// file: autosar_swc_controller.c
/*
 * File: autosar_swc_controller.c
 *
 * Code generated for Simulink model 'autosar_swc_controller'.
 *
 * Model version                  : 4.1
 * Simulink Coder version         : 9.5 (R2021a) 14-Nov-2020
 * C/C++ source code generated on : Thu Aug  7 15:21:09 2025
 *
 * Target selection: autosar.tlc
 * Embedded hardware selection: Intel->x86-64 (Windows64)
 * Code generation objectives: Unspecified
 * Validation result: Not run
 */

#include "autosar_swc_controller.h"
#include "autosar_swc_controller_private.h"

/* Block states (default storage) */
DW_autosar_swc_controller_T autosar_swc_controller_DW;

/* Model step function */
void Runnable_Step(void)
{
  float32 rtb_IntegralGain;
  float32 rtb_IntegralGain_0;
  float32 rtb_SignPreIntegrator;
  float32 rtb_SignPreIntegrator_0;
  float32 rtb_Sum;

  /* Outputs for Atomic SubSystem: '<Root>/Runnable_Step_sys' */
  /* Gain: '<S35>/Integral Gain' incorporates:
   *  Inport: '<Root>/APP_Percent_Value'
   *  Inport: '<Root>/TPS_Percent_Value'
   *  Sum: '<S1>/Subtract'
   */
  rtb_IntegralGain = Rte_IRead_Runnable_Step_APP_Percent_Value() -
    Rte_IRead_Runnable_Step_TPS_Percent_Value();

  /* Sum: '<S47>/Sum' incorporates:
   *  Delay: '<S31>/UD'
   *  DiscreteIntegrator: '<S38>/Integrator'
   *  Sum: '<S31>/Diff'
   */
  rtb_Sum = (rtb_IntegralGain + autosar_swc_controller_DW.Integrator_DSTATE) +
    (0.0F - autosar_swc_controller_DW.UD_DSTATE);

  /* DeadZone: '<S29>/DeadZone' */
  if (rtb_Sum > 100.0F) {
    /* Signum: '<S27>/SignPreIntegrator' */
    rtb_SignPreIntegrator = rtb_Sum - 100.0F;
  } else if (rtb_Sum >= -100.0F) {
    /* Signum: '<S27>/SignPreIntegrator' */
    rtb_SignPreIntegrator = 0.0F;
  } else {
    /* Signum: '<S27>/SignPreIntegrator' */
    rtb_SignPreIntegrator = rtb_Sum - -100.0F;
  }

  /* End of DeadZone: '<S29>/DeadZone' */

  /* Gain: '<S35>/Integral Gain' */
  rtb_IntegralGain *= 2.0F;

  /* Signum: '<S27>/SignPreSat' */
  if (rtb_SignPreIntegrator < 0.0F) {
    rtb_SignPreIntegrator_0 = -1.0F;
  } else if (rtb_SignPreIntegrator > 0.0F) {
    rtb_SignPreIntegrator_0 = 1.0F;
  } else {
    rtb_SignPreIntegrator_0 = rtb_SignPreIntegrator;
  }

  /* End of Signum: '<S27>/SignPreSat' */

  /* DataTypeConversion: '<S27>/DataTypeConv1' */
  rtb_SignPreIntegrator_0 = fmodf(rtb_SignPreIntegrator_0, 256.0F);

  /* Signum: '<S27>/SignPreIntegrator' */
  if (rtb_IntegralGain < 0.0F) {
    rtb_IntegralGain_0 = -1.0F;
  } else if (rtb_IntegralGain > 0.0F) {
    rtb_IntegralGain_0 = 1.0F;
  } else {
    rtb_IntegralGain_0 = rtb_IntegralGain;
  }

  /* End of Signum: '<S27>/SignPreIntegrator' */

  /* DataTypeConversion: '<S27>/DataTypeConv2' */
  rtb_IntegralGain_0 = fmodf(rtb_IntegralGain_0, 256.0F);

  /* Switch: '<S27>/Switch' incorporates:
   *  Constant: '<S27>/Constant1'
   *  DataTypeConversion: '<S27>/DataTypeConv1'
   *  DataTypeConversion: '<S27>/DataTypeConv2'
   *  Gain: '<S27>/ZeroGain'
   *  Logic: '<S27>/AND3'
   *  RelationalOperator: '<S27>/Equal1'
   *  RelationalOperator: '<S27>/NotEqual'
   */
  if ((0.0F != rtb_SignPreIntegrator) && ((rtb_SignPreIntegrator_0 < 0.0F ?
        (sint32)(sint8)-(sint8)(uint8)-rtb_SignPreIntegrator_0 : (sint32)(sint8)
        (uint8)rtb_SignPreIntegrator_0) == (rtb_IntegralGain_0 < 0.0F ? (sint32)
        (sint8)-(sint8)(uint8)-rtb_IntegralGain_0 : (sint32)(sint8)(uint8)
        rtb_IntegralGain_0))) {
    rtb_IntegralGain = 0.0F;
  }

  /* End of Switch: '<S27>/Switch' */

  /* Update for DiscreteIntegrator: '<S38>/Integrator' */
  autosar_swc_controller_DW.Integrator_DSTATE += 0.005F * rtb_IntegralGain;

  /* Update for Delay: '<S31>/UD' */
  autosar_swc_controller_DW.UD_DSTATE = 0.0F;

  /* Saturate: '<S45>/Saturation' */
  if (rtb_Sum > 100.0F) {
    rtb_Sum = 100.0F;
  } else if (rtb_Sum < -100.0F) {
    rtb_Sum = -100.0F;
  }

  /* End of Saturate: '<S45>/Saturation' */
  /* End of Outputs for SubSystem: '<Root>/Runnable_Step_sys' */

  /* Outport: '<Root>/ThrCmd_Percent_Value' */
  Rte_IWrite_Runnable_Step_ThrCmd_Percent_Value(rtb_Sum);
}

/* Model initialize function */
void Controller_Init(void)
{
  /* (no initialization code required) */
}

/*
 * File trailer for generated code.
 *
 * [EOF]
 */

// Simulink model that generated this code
simulink model "autosar_swc_controller"  (R2021a)
settings: Solver=FixedStepDiscrete  StartTime=0.0  StopTime=10.0  FixedStep=0.005  RelTol=1e-3
libraries: pid_lib x1

== system autosar_swc_controller ==
  note: Copyright 2017 The MathWorks, Inc.
  TPS_Percent_Value : Inport  OutDataTypeStr=single  PortDimensions=1
  APP_Percent_Value : Inport  Port=2  OutDataTypeStr=single  PortDimensions=1
  Runnable_Step_sys : Subsystem  TreatAsAtomicUnit=on  SystemSampleTime=0.005
  ThrCmd_Percent_Value : Outport  OutDataTypeStr=single  PortDimensions=1  VectorParamsAs1DForOutWhenUnconnected=off
  wires:
  TPS_Percent_Value/1 -> Runnable_Step_sys/1(TPS_Percent_Value_read)
  APP_Percent_Value/1 -> Runnable_Step_sys/2(APP_Percent_Value_read)
  Runnable_Step_sys/1(ThrCmd_Percent_Value_write) -> ThrCmd_Percent_Value/1

== system autosar_swc_controller/Runnable_Step_sys ==
  TPS_Percent_Value_read : Inport
  APP_Percent_Value_read : Inport  Port=2
  Discrete PID Controller : pid_lib/PID Controller  Controller=PID  Form=Parallel  TimeDomain=Discrete-time  UseExternalTs=off  SampleTime=-1  IntegratorMethod=Forward Euler  FilterMethod=Forward Euler  ControllerParametersSource=internal  P=1  I=2  D=0  UseFilter=off  N=100  TunerSelectOption=Transfer Function Based (PID Tuner App)  InitialConditionSource=internal  InitialConditionForIntegrator=0  InitialConditionForFilter=0  DifferentiatorICPrevScaledInput=0  ExternalReset=none  TrackingMode=off  Kt=1  LimitOutput=on  SatLimitsSource=internal  UpperSaturationLimit=100  LowerSaturationLimit=-100  LinearizeAsGain=off  AntiWindupMode=clamping  Kb=1  POutMin=[]  POutMax=[]  IOutMin=[]  IOutMax=[]  DOutMin=[]  DOutMax=[]  NOutMin=[]  NOutMax=[]  SumOutMin=[]  SumOutMax=[]  SaturationOutMin=[]  SaturationOutMax=[]  PParamMin=[]  PParamMax=[]  IParamMin=[]  IParamMax=[]  DParamMin=[]  DParamMax=[]  NParamMin=[]  NParamMax=[]  KbParamMin=[]  KbParamMax=[]  KtParamMin=[]  KtParamMax=[]  KbOutMin=[]  KbOutMax=[]  KtOutMin=[]  KtOutMax=[]  IntegratorOutMin=[]  IntegratorOutMax=[]  FilterOutMin=[]  FilterOutMax=[]  SumI1OutMin=[]  SumI1OutMax=[]  SumI2OutMin=[]  SumI2OutMax=[]  SumI3OutMin=[]  SumI3OutMax=[]  SumI4OutMin=[]  SumI4OutMax=[]  SumDOutMin=[]  SumDOutMax=[]  DifferentiatorOutMin=[]  DifferentiatorOutMax=[]  FilterDiffOutCoefMin=[]  FilterDiffOutCoefMax=[]  ReciprocalOutMin=[]  ReciprocalOutMax=[]  SumDenOutMin=[]  SumDenOutMax=[]  SumNumOutMin=[]  SumNumOutMax=[]  DivideOutMin=[]  DivideOutMax=[]  UdiffTsProdOutMin=[]  UdiffTsProdOutMax=[]  NTsProdOutMin=[]  NTsProdOutMax=[]  UintegralTsProdOutMin=[]  UintegralTsProdOutMax=[]  UngainTsProdOutMin=[]  UngainTsProdOutMax=[]  IntegratorContinuousStateAttributes=''  IntegratorStateMustResolveToSignalObject=off  IntegratorRTWStateStorageClass=Auto  FilterContinuousStateAttributes=''  FilterStateMustResolveToSignalObject=off  FilterRTWStateStorageClass=Auto  ParallelPVariant=InternalParameters  IdealPVariant=Disabled  IVariant=InternalParameters  DVariant=InternalParameters  IntegratorVariant=Discrete  SatVariant=Enabled  AWVariant=DiscClampingParallel  PCopyVariant=Disabled  TRVariant=Disabled  FdbkBlocksVariant=Forward  IdealPFdbkVariant=Disabled  SatFdbkVariant=Disabled  DerivativeFilterVariant=Differentiator  NVariant=Passthrough  NCopyVariant=Disabled_SignalSpec  FilterICVariant=InternalICsDifferentiator  IntegratorICVariant=InternalICs  ExternalResetVariant=Disabled  TRSumVariant=Passthrough  SumFdbkVariant=Disabled  SumVariant=Sum_PID  TsampFilterVariant=InternalTs  TsampNgainVariant=Passthrough  TsampIntegralVariant=Passthrough  ExternalSaturationOutDataTypeStr=Inherit: Same as second input
  Scope : Scope  NumInputPorts=4
  Subtract : Sum  Inputs=+-
  ThrCmd_Percent_Value_write : Outport  VectorParamsAs1DForOutWhenUnconnected=off
  wires:
  TPS_Percent_Value_read/1 -> Scope/3, Subtract/2
  APP_Percent_Value_read/1 -> Scope/2, Subtract/1
  Discrete PID Controller/1 -> Scope/4, ThrCmd_Percent_Value_write/1
  Subtract/1 -> Scope/1, Discrete PID Controller/1  "error"
